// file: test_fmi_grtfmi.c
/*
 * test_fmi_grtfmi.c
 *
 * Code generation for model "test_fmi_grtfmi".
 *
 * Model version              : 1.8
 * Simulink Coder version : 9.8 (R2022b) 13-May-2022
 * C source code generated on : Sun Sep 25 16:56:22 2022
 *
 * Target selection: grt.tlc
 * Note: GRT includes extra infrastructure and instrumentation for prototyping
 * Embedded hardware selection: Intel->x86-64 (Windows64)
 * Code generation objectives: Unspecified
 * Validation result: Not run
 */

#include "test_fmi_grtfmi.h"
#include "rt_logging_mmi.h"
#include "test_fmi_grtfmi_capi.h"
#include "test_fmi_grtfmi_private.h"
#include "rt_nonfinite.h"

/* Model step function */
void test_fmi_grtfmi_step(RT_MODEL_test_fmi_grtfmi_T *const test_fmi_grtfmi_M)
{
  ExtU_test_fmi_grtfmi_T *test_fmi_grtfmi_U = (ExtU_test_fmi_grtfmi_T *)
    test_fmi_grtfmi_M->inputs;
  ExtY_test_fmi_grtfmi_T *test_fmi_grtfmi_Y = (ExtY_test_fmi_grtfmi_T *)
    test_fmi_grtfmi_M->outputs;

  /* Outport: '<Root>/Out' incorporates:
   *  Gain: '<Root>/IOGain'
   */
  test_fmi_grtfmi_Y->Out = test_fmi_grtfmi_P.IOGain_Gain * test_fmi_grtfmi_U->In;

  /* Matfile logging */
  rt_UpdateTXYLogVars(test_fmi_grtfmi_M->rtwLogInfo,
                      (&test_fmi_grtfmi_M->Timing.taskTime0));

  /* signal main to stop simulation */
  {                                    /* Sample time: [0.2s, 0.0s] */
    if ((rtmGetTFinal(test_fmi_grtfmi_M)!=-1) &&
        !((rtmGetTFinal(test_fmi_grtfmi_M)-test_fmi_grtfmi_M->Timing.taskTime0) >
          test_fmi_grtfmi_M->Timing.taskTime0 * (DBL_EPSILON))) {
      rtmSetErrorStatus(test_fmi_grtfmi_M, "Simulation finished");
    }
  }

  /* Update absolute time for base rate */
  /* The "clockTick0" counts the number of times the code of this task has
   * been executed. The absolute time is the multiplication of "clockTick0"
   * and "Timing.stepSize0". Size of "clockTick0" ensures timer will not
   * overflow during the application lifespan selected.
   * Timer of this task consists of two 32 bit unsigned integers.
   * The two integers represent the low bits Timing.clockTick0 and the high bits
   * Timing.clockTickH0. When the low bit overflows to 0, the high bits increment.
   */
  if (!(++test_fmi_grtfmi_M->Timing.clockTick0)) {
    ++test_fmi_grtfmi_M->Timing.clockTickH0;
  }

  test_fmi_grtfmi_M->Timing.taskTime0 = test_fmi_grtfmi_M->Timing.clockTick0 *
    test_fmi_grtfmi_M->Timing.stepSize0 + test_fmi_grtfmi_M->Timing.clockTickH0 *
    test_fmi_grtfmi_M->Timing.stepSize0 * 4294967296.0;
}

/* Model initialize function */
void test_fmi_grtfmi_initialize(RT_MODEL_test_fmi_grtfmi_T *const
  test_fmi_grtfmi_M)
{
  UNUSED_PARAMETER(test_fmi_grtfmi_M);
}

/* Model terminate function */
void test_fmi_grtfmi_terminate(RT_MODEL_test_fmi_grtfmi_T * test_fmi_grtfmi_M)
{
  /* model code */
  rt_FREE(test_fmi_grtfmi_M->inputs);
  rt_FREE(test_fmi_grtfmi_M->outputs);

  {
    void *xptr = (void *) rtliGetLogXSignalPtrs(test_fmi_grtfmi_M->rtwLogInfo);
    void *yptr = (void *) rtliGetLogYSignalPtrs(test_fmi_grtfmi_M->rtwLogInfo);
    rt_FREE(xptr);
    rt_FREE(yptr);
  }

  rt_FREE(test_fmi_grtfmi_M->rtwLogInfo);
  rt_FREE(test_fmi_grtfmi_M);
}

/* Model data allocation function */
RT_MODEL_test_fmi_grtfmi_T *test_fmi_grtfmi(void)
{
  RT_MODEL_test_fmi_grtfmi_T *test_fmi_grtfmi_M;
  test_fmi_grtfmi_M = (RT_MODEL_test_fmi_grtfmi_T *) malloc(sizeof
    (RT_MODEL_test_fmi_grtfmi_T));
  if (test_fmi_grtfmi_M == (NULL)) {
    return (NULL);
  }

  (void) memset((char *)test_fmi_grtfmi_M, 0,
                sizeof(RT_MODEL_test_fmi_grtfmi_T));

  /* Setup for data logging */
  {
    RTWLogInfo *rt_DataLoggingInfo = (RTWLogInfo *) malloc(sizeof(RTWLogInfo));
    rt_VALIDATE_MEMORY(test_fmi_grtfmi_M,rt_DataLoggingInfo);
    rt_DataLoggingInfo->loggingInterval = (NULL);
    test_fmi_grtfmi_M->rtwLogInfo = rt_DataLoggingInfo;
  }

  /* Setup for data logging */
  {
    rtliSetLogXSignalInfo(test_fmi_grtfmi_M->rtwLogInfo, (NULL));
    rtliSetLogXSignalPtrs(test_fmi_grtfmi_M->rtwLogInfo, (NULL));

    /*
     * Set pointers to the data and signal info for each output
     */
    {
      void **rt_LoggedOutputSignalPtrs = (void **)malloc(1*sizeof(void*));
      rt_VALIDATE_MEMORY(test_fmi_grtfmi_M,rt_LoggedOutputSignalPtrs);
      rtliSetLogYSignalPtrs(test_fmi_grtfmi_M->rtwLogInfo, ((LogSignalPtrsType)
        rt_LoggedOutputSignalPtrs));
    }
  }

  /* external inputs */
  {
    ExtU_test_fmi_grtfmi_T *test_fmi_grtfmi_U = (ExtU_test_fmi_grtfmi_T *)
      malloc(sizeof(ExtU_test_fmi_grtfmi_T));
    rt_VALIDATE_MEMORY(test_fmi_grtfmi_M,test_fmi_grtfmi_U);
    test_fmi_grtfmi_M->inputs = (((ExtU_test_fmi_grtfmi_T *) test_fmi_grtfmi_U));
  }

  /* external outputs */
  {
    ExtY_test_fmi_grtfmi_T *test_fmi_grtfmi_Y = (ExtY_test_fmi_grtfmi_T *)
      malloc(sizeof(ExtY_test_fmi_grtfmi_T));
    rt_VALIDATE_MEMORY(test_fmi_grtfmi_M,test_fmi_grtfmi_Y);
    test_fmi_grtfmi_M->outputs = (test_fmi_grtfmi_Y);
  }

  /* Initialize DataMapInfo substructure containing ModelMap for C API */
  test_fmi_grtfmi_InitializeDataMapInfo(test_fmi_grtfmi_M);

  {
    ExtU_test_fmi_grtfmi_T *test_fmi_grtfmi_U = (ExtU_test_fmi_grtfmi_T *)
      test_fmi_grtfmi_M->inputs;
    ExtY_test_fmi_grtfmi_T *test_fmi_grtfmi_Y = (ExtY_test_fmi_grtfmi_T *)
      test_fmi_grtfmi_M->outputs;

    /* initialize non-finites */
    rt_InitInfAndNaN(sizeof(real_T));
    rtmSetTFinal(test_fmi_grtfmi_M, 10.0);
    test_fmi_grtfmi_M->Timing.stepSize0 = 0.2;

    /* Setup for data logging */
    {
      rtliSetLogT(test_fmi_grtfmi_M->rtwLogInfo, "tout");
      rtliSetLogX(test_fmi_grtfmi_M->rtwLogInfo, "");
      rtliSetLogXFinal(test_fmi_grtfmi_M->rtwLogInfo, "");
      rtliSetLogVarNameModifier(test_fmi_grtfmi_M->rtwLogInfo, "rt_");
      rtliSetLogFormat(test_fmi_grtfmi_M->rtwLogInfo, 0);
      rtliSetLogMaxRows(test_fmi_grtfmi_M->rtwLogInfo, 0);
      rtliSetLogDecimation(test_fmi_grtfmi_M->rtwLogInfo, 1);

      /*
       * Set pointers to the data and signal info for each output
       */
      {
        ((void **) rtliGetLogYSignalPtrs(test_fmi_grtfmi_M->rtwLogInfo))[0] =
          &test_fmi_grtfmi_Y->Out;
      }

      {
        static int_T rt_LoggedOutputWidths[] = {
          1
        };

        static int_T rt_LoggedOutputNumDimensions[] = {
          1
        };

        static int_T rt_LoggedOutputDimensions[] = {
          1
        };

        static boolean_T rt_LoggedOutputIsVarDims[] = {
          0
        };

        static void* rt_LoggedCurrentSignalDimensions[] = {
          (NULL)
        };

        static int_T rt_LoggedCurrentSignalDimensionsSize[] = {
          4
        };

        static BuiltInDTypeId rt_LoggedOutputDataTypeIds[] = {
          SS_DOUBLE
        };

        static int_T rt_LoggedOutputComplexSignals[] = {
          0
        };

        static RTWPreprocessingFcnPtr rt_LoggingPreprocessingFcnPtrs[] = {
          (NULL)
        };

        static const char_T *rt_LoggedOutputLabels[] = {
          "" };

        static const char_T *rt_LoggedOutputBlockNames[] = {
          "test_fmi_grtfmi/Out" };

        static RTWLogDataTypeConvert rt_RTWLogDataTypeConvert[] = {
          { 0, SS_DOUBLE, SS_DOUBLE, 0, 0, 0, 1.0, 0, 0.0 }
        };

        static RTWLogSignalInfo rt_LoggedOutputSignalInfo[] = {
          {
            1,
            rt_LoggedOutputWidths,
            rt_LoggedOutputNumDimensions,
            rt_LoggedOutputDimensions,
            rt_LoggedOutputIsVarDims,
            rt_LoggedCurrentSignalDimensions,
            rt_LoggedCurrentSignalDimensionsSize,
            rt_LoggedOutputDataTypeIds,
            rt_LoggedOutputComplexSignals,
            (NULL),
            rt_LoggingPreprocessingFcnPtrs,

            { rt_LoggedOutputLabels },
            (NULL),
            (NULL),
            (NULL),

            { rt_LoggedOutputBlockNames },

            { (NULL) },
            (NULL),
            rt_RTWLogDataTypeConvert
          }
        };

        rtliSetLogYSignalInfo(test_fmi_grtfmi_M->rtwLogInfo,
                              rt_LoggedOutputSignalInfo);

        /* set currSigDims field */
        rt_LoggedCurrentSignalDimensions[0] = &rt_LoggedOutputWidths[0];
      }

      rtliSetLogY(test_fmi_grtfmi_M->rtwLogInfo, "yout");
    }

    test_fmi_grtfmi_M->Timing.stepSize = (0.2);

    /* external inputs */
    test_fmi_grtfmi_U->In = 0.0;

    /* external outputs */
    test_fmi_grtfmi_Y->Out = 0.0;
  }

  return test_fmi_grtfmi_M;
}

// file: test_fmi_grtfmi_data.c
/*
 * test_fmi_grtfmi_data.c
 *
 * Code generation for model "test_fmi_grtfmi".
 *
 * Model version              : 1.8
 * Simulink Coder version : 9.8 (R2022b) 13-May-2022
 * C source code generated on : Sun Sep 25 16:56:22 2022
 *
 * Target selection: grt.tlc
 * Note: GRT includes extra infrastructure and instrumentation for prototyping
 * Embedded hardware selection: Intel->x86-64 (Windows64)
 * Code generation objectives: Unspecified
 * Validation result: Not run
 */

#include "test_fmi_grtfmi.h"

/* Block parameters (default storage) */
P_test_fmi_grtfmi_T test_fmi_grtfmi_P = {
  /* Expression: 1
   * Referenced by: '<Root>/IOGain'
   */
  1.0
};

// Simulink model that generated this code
simulink model "test_fmi_grtfmi"  (R2022b)
settings: Solver=FixedStepAuto  StartTime=0.0  StopTime=10.0  RelTol=1e-3
PreLoadFcn:
  | fmi_init;
  | init;

== system test_fmi_grtfmi ==
  In : Inport
  IOGain : Gain
  Out : Outport
  wires:
  In/1 -> IOGain/1
  IOGain/1 -> Out/1
